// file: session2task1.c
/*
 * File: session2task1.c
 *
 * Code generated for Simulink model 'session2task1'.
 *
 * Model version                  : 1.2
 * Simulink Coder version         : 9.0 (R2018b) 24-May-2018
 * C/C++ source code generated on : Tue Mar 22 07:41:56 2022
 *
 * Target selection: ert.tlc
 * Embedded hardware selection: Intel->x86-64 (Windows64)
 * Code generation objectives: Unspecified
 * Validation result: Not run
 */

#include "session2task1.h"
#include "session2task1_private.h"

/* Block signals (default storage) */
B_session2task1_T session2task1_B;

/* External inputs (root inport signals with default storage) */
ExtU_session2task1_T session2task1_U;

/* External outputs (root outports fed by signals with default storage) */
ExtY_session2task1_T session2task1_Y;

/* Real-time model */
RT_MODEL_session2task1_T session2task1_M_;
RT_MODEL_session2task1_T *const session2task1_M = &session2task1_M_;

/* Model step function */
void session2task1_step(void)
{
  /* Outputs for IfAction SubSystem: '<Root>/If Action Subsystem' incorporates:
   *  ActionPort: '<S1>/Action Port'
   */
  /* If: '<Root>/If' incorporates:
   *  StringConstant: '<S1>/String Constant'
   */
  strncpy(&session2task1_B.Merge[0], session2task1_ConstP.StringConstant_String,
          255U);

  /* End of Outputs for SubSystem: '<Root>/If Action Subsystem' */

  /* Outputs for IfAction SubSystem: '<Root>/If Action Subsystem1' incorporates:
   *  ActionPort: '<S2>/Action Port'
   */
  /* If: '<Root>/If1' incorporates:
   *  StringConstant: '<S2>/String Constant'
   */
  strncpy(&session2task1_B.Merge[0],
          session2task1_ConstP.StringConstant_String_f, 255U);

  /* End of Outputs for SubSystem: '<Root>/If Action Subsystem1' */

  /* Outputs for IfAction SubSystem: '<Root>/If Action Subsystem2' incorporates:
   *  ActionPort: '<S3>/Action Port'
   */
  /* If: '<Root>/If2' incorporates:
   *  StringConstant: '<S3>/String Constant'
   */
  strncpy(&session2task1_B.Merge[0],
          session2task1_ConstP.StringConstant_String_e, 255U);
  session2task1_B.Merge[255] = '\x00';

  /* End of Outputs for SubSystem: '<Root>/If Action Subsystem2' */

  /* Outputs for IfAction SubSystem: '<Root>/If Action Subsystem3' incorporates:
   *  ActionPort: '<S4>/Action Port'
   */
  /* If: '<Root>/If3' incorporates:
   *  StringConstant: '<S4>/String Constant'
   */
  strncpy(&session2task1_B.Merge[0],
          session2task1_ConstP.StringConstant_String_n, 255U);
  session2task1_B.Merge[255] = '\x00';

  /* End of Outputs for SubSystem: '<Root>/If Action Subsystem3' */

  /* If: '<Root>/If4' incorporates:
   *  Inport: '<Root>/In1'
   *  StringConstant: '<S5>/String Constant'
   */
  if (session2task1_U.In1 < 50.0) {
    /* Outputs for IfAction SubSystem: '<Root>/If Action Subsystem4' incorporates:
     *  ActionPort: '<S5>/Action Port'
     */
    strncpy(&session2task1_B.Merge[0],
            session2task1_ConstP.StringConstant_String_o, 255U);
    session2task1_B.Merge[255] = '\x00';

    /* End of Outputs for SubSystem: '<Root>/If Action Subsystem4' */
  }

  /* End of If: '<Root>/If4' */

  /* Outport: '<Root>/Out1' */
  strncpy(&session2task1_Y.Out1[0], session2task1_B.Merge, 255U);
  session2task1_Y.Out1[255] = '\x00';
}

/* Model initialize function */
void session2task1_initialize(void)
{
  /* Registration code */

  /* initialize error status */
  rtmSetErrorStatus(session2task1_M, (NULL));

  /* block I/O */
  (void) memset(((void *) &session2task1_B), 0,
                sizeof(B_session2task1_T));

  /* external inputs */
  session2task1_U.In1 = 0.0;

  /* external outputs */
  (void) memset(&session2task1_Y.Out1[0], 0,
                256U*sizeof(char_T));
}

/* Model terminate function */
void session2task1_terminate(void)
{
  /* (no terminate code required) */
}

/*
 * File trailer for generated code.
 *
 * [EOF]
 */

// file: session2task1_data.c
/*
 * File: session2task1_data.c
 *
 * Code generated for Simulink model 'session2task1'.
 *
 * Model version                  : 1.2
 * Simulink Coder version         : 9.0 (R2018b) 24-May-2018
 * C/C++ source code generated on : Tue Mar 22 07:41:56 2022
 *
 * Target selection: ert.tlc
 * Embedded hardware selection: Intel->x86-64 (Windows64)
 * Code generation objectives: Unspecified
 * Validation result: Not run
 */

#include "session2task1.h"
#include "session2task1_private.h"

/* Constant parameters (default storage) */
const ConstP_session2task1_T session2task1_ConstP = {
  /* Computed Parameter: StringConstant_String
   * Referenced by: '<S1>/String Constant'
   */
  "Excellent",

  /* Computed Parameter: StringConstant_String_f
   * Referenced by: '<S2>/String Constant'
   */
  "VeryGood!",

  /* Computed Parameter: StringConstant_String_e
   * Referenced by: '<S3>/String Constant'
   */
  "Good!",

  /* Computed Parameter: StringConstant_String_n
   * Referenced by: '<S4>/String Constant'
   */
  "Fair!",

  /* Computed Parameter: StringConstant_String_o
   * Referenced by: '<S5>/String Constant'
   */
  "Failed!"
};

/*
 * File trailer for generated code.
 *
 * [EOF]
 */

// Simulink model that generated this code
simulink model "session2task1"  (R2018b)
settings: Solver=FixedStepDiscrete  StartTime=0.0  StopTime=10.0  RelTol=1e-3

== system session2task1 ==
  In1 : Inport
  If : If  IfExpression=85 > u1 < 100
  If Action Subsystem : Subsystem  TreatAsAtomicUnit=on
  If Action Subsystem1 : Subsystem  TreatAsAtomicUnit=on
  If Action Subsystem2 : Subsystem  TreatAsAtomicUnit=on
  If Action Subsystem3 : Subsystem  TreatAsAtomicUnit=on
  If Action Subsystem4 : Subsystem  TreatAsAtomicUnit=on
  If1 : If  IfExpression=75 > u1 < 85
  If2 : If  IfExpression=65 > u1 < 75
  If3 : If  IfExpression=50 > u1 < 65
  If4 : If  IfExpression=u1 < 50
  Merge : Merge  Inputs=5
  Out1 : Outport
  wires:
  If/1 -> If Action Subsystem/Action
  If1/1 -> If Action Subsystem1/Action
  If2/1 -> If Action Subsystem2/Action
  If3/1 -> If Action Subsystem3/Action
  If4/1 -> If Action Subsystem4/Action
  Merge/1 -> Out1/1
  If Action Subsystem/1(Out1) -> Merge/1
  If Action Subsystem1/1(Out1) -> Merge/2
  If Action Subsystem2/1(Out1) -> Merge/3
  If Action Subsystem3/1(Out1) -> Merge/4
  If Action Subsystem4/1(Out1) -> Merge/5
  In1/1 -> If4/1, If1/1, If/1, If2/1, If3/1

== system session2task1/If Action Subsystem ==
  Action Port : ActionPort  ActionType=then
  String Constant : StringConstant  String="\"Excellent\""
  Out1 : Outport
  wires:
  String Constant/1 -> Out1/1

== system session2task1/If Action Subsystem1 ==
  Action Port : ActionPort  ActionType=then
  String Constant : StringConstant  String="\"VeryGood!\""
  Out1 : Outport
  wires:
  String Constant/1 -> Out1/1

== system session2task1/If Action Subsystem2 ==
  Action Port : ActionPort  ActionType=then
  String Constant : StringConstant  String="\"Good!\""
  Out1 : Outport
  wires:
  String Constant/1 -> Out1/1

== system session2task1/If Action Subsystem3 ==
  Action Port : ActionPort  ActionType=then
  String Constant : StringConstant  String="\"Fair!\""
  Out1 : Outport
  wires:
  String Constant/1 -> Out1/1

== system session2task1/If Action Subsystem4 ==
  Action Port : ActionPort  ActionType=then
  String Constant : StringConstant  String="\"Failed!\""
  Out1 : Outport
  wires:
  String Constant/1 -> Out1/1
